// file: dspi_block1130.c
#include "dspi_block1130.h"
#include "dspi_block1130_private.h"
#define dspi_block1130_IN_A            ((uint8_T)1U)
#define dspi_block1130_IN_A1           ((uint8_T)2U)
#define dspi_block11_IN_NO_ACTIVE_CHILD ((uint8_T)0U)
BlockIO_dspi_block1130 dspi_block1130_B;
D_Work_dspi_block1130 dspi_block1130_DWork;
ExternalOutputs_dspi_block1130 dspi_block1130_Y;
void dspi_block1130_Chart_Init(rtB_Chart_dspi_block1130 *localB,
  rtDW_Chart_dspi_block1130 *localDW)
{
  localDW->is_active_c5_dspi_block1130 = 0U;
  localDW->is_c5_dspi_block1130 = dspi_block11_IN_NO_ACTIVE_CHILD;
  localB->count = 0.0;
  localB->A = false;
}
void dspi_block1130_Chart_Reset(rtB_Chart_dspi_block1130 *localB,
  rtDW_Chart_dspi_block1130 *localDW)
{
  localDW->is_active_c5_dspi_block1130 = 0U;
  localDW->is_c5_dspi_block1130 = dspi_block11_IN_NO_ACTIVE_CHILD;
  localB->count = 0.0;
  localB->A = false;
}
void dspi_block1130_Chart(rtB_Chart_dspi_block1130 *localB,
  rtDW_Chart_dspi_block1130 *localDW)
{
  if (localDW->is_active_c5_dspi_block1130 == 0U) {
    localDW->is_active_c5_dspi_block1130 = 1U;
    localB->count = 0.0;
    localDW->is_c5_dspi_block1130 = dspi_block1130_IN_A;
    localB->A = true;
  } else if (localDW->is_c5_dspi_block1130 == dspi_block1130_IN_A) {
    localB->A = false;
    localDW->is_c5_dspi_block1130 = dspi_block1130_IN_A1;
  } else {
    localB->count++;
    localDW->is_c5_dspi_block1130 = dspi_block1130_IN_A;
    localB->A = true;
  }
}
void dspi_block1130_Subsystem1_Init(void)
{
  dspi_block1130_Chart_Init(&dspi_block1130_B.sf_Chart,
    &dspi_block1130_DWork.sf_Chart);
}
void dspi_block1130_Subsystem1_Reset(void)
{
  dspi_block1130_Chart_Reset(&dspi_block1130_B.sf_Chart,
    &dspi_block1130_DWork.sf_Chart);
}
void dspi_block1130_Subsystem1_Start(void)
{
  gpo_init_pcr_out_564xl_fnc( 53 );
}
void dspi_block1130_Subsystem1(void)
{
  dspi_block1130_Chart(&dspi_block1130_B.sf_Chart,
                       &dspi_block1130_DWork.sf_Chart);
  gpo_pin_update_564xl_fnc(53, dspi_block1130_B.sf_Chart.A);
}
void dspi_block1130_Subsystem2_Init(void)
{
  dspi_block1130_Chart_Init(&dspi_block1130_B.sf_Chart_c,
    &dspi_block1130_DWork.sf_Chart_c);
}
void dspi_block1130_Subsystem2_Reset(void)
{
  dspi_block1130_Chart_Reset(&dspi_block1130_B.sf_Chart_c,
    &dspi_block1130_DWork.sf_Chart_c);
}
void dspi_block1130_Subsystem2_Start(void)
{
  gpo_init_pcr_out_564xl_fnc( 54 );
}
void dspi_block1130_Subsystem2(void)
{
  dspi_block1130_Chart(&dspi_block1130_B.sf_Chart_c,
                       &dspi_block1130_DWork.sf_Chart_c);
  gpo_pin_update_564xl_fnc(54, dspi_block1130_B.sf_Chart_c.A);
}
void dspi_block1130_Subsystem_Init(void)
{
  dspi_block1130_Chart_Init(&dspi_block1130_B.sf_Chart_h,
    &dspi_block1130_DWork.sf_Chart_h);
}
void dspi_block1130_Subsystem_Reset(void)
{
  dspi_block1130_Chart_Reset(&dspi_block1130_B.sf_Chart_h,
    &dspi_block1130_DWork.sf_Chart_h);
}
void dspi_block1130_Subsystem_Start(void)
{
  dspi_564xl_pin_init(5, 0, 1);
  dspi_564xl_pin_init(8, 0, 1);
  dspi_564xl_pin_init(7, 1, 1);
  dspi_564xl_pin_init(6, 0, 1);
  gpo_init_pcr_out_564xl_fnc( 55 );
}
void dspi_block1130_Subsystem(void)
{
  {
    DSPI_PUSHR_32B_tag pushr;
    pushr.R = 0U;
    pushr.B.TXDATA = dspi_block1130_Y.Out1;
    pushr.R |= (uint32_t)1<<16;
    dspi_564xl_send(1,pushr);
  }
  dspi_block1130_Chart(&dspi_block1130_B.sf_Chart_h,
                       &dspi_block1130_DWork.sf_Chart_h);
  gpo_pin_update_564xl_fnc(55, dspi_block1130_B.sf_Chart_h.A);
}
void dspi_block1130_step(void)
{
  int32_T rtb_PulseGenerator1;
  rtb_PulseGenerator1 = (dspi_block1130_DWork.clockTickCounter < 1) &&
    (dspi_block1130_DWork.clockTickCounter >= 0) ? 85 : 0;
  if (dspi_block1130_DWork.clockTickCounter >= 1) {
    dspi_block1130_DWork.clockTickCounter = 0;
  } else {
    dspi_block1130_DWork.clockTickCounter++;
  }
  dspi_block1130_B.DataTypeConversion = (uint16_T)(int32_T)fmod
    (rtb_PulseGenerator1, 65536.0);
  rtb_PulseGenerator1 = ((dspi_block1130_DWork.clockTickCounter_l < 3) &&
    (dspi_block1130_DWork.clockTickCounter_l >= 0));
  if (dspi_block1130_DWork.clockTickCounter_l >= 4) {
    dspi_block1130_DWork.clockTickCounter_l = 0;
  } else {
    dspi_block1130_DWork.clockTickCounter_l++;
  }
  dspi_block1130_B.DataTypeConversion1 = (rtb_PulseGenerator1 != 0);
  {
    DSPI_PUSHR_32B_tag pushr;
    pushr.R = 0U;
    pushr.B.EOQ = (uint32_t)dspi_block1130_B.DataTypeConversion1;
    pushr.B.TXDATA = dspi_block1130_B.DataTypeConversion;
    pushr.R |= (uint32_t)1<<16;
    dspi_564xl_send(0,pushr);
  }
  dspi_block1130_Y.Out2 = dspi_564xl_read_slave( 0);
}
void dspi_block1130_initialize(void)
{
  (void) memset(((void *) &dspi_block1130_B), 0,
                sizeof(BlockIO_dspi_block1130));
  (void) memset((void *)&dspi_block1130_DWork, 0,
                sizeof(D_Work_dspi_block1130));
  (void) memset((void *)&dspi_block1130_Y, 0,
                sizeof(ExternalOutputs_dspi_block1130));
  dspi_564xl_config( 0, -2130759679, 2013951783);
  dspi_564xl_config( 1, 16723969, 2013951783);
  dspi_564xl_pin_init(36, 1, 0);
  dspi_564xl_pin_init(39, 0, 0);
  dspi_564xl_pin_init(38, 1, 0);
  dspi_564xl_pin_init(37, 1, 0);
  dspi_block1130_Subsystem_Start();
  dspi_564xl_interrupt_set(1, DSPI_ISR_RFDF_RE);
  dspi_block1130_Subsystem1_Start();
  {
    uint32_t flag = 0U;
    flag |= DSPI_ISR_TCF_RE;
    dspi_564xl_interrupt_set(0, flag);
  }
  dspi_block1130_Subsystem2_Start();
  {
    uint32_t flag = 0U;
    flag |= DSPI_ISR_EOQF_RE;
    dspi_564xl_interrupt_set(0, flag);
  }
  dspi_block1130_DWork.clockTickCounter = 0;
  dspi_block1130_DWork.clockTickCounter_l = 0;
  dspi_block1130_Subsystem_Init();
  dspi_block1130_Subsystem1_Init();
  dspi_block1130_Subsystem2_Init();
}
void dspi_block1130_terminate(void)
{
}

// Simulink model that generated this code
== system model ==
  Out2 : Outport  <- 1: DSPIReceive#1
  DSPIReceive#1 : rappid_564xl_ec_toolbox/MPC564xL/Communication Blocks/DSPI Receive
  Out1 : Outport  <- 1: DSPIReceiveTrigger#1/2
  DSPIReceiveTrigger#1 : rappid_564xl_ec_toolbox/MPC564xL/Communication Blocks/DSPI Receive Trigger
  Subsystem1 : Subsystem  <- Trigger: DSPIISR#1
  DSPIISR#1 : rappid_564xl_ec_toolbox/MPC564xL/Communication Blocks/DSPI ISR
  Subsystem2 : Subsystem  <- Trigger: DSPIISR#2
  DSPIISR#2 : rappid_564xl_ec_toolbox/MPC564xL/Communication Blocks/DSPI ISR
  Subsystem : Subsystem  <- 1: DSPIReceiveTrigger#1/2, Trigger: DSPIReceiveTrigger#1
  DSPITransmit#1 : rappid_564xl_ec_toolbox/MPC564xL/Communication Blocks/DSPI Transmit  <- 1: DataTypeConversion, 2: DataTypeConversion1
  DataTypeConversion : DataTypeConversion  <- 1: DiscretePulseGenerator#1
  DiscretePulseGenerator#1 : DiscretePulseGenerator  Amplitude=85
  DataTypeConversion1 : DataTypeConversion  <- 1: PulseGenerator1
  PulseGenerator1 : DiscretePulseGenerator  Period=5  PulseWidth=3
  DSPIConfig#1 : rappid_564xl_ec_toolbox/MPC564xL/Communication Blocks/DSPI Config
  DSPIConfig#2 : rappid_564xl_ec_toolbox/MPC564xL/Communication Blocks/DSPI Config
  RAppID_564xL_Config#1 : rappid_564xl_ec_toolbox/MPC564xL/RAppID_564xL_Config
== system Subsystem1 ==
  TriggerPort#1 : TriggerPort  TriggerType=function-call
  DigitalOutput#1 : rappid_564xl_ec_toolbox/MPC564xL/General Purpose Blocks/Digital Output  <- 1: Chart/2
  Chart : Stateflow chart
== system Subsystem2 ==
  TriggerPort#2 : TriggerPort  TriggerType=function-call
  DigitalOutput#2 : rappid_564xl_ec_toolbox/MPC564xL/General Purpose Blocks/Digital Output  <- 1: Stateflowchart#1/2
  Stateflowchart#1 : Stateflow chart
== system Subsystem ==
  Inport#1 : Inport
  TriggerPort#3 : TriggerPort  TriggerType=function-call
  DigitalOutput#3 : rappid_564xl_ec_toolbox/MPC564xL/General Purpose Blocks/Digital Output  <- 1: Stateflowchart#2/2
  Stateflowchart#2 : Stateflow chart
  DSPITransmit#2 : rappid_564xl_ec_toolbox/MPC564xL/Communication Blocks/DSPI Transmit  <- 1: Inport#1
== stateflow chart Chart ==
  state A
  state A1
  (default) -> A : {count =0;}
  A -> A1
  A1 -> A : { count = count + 1;}
  data: count output double; A output boolean

== stateflow chart Chart ==
  state A
  state A1
  (default) -> A : {count =0;}
  A -> A1
  A1 -> A : { count = count + 1;}
  data: count output double; A output boolean

== stateflow chart Chart ==
  state A
  state A1
  (default) -> A : {count =0;}
  A -> A1
  A1 -> A : { count = count + 1;}
  data: count output double; A output boolean
